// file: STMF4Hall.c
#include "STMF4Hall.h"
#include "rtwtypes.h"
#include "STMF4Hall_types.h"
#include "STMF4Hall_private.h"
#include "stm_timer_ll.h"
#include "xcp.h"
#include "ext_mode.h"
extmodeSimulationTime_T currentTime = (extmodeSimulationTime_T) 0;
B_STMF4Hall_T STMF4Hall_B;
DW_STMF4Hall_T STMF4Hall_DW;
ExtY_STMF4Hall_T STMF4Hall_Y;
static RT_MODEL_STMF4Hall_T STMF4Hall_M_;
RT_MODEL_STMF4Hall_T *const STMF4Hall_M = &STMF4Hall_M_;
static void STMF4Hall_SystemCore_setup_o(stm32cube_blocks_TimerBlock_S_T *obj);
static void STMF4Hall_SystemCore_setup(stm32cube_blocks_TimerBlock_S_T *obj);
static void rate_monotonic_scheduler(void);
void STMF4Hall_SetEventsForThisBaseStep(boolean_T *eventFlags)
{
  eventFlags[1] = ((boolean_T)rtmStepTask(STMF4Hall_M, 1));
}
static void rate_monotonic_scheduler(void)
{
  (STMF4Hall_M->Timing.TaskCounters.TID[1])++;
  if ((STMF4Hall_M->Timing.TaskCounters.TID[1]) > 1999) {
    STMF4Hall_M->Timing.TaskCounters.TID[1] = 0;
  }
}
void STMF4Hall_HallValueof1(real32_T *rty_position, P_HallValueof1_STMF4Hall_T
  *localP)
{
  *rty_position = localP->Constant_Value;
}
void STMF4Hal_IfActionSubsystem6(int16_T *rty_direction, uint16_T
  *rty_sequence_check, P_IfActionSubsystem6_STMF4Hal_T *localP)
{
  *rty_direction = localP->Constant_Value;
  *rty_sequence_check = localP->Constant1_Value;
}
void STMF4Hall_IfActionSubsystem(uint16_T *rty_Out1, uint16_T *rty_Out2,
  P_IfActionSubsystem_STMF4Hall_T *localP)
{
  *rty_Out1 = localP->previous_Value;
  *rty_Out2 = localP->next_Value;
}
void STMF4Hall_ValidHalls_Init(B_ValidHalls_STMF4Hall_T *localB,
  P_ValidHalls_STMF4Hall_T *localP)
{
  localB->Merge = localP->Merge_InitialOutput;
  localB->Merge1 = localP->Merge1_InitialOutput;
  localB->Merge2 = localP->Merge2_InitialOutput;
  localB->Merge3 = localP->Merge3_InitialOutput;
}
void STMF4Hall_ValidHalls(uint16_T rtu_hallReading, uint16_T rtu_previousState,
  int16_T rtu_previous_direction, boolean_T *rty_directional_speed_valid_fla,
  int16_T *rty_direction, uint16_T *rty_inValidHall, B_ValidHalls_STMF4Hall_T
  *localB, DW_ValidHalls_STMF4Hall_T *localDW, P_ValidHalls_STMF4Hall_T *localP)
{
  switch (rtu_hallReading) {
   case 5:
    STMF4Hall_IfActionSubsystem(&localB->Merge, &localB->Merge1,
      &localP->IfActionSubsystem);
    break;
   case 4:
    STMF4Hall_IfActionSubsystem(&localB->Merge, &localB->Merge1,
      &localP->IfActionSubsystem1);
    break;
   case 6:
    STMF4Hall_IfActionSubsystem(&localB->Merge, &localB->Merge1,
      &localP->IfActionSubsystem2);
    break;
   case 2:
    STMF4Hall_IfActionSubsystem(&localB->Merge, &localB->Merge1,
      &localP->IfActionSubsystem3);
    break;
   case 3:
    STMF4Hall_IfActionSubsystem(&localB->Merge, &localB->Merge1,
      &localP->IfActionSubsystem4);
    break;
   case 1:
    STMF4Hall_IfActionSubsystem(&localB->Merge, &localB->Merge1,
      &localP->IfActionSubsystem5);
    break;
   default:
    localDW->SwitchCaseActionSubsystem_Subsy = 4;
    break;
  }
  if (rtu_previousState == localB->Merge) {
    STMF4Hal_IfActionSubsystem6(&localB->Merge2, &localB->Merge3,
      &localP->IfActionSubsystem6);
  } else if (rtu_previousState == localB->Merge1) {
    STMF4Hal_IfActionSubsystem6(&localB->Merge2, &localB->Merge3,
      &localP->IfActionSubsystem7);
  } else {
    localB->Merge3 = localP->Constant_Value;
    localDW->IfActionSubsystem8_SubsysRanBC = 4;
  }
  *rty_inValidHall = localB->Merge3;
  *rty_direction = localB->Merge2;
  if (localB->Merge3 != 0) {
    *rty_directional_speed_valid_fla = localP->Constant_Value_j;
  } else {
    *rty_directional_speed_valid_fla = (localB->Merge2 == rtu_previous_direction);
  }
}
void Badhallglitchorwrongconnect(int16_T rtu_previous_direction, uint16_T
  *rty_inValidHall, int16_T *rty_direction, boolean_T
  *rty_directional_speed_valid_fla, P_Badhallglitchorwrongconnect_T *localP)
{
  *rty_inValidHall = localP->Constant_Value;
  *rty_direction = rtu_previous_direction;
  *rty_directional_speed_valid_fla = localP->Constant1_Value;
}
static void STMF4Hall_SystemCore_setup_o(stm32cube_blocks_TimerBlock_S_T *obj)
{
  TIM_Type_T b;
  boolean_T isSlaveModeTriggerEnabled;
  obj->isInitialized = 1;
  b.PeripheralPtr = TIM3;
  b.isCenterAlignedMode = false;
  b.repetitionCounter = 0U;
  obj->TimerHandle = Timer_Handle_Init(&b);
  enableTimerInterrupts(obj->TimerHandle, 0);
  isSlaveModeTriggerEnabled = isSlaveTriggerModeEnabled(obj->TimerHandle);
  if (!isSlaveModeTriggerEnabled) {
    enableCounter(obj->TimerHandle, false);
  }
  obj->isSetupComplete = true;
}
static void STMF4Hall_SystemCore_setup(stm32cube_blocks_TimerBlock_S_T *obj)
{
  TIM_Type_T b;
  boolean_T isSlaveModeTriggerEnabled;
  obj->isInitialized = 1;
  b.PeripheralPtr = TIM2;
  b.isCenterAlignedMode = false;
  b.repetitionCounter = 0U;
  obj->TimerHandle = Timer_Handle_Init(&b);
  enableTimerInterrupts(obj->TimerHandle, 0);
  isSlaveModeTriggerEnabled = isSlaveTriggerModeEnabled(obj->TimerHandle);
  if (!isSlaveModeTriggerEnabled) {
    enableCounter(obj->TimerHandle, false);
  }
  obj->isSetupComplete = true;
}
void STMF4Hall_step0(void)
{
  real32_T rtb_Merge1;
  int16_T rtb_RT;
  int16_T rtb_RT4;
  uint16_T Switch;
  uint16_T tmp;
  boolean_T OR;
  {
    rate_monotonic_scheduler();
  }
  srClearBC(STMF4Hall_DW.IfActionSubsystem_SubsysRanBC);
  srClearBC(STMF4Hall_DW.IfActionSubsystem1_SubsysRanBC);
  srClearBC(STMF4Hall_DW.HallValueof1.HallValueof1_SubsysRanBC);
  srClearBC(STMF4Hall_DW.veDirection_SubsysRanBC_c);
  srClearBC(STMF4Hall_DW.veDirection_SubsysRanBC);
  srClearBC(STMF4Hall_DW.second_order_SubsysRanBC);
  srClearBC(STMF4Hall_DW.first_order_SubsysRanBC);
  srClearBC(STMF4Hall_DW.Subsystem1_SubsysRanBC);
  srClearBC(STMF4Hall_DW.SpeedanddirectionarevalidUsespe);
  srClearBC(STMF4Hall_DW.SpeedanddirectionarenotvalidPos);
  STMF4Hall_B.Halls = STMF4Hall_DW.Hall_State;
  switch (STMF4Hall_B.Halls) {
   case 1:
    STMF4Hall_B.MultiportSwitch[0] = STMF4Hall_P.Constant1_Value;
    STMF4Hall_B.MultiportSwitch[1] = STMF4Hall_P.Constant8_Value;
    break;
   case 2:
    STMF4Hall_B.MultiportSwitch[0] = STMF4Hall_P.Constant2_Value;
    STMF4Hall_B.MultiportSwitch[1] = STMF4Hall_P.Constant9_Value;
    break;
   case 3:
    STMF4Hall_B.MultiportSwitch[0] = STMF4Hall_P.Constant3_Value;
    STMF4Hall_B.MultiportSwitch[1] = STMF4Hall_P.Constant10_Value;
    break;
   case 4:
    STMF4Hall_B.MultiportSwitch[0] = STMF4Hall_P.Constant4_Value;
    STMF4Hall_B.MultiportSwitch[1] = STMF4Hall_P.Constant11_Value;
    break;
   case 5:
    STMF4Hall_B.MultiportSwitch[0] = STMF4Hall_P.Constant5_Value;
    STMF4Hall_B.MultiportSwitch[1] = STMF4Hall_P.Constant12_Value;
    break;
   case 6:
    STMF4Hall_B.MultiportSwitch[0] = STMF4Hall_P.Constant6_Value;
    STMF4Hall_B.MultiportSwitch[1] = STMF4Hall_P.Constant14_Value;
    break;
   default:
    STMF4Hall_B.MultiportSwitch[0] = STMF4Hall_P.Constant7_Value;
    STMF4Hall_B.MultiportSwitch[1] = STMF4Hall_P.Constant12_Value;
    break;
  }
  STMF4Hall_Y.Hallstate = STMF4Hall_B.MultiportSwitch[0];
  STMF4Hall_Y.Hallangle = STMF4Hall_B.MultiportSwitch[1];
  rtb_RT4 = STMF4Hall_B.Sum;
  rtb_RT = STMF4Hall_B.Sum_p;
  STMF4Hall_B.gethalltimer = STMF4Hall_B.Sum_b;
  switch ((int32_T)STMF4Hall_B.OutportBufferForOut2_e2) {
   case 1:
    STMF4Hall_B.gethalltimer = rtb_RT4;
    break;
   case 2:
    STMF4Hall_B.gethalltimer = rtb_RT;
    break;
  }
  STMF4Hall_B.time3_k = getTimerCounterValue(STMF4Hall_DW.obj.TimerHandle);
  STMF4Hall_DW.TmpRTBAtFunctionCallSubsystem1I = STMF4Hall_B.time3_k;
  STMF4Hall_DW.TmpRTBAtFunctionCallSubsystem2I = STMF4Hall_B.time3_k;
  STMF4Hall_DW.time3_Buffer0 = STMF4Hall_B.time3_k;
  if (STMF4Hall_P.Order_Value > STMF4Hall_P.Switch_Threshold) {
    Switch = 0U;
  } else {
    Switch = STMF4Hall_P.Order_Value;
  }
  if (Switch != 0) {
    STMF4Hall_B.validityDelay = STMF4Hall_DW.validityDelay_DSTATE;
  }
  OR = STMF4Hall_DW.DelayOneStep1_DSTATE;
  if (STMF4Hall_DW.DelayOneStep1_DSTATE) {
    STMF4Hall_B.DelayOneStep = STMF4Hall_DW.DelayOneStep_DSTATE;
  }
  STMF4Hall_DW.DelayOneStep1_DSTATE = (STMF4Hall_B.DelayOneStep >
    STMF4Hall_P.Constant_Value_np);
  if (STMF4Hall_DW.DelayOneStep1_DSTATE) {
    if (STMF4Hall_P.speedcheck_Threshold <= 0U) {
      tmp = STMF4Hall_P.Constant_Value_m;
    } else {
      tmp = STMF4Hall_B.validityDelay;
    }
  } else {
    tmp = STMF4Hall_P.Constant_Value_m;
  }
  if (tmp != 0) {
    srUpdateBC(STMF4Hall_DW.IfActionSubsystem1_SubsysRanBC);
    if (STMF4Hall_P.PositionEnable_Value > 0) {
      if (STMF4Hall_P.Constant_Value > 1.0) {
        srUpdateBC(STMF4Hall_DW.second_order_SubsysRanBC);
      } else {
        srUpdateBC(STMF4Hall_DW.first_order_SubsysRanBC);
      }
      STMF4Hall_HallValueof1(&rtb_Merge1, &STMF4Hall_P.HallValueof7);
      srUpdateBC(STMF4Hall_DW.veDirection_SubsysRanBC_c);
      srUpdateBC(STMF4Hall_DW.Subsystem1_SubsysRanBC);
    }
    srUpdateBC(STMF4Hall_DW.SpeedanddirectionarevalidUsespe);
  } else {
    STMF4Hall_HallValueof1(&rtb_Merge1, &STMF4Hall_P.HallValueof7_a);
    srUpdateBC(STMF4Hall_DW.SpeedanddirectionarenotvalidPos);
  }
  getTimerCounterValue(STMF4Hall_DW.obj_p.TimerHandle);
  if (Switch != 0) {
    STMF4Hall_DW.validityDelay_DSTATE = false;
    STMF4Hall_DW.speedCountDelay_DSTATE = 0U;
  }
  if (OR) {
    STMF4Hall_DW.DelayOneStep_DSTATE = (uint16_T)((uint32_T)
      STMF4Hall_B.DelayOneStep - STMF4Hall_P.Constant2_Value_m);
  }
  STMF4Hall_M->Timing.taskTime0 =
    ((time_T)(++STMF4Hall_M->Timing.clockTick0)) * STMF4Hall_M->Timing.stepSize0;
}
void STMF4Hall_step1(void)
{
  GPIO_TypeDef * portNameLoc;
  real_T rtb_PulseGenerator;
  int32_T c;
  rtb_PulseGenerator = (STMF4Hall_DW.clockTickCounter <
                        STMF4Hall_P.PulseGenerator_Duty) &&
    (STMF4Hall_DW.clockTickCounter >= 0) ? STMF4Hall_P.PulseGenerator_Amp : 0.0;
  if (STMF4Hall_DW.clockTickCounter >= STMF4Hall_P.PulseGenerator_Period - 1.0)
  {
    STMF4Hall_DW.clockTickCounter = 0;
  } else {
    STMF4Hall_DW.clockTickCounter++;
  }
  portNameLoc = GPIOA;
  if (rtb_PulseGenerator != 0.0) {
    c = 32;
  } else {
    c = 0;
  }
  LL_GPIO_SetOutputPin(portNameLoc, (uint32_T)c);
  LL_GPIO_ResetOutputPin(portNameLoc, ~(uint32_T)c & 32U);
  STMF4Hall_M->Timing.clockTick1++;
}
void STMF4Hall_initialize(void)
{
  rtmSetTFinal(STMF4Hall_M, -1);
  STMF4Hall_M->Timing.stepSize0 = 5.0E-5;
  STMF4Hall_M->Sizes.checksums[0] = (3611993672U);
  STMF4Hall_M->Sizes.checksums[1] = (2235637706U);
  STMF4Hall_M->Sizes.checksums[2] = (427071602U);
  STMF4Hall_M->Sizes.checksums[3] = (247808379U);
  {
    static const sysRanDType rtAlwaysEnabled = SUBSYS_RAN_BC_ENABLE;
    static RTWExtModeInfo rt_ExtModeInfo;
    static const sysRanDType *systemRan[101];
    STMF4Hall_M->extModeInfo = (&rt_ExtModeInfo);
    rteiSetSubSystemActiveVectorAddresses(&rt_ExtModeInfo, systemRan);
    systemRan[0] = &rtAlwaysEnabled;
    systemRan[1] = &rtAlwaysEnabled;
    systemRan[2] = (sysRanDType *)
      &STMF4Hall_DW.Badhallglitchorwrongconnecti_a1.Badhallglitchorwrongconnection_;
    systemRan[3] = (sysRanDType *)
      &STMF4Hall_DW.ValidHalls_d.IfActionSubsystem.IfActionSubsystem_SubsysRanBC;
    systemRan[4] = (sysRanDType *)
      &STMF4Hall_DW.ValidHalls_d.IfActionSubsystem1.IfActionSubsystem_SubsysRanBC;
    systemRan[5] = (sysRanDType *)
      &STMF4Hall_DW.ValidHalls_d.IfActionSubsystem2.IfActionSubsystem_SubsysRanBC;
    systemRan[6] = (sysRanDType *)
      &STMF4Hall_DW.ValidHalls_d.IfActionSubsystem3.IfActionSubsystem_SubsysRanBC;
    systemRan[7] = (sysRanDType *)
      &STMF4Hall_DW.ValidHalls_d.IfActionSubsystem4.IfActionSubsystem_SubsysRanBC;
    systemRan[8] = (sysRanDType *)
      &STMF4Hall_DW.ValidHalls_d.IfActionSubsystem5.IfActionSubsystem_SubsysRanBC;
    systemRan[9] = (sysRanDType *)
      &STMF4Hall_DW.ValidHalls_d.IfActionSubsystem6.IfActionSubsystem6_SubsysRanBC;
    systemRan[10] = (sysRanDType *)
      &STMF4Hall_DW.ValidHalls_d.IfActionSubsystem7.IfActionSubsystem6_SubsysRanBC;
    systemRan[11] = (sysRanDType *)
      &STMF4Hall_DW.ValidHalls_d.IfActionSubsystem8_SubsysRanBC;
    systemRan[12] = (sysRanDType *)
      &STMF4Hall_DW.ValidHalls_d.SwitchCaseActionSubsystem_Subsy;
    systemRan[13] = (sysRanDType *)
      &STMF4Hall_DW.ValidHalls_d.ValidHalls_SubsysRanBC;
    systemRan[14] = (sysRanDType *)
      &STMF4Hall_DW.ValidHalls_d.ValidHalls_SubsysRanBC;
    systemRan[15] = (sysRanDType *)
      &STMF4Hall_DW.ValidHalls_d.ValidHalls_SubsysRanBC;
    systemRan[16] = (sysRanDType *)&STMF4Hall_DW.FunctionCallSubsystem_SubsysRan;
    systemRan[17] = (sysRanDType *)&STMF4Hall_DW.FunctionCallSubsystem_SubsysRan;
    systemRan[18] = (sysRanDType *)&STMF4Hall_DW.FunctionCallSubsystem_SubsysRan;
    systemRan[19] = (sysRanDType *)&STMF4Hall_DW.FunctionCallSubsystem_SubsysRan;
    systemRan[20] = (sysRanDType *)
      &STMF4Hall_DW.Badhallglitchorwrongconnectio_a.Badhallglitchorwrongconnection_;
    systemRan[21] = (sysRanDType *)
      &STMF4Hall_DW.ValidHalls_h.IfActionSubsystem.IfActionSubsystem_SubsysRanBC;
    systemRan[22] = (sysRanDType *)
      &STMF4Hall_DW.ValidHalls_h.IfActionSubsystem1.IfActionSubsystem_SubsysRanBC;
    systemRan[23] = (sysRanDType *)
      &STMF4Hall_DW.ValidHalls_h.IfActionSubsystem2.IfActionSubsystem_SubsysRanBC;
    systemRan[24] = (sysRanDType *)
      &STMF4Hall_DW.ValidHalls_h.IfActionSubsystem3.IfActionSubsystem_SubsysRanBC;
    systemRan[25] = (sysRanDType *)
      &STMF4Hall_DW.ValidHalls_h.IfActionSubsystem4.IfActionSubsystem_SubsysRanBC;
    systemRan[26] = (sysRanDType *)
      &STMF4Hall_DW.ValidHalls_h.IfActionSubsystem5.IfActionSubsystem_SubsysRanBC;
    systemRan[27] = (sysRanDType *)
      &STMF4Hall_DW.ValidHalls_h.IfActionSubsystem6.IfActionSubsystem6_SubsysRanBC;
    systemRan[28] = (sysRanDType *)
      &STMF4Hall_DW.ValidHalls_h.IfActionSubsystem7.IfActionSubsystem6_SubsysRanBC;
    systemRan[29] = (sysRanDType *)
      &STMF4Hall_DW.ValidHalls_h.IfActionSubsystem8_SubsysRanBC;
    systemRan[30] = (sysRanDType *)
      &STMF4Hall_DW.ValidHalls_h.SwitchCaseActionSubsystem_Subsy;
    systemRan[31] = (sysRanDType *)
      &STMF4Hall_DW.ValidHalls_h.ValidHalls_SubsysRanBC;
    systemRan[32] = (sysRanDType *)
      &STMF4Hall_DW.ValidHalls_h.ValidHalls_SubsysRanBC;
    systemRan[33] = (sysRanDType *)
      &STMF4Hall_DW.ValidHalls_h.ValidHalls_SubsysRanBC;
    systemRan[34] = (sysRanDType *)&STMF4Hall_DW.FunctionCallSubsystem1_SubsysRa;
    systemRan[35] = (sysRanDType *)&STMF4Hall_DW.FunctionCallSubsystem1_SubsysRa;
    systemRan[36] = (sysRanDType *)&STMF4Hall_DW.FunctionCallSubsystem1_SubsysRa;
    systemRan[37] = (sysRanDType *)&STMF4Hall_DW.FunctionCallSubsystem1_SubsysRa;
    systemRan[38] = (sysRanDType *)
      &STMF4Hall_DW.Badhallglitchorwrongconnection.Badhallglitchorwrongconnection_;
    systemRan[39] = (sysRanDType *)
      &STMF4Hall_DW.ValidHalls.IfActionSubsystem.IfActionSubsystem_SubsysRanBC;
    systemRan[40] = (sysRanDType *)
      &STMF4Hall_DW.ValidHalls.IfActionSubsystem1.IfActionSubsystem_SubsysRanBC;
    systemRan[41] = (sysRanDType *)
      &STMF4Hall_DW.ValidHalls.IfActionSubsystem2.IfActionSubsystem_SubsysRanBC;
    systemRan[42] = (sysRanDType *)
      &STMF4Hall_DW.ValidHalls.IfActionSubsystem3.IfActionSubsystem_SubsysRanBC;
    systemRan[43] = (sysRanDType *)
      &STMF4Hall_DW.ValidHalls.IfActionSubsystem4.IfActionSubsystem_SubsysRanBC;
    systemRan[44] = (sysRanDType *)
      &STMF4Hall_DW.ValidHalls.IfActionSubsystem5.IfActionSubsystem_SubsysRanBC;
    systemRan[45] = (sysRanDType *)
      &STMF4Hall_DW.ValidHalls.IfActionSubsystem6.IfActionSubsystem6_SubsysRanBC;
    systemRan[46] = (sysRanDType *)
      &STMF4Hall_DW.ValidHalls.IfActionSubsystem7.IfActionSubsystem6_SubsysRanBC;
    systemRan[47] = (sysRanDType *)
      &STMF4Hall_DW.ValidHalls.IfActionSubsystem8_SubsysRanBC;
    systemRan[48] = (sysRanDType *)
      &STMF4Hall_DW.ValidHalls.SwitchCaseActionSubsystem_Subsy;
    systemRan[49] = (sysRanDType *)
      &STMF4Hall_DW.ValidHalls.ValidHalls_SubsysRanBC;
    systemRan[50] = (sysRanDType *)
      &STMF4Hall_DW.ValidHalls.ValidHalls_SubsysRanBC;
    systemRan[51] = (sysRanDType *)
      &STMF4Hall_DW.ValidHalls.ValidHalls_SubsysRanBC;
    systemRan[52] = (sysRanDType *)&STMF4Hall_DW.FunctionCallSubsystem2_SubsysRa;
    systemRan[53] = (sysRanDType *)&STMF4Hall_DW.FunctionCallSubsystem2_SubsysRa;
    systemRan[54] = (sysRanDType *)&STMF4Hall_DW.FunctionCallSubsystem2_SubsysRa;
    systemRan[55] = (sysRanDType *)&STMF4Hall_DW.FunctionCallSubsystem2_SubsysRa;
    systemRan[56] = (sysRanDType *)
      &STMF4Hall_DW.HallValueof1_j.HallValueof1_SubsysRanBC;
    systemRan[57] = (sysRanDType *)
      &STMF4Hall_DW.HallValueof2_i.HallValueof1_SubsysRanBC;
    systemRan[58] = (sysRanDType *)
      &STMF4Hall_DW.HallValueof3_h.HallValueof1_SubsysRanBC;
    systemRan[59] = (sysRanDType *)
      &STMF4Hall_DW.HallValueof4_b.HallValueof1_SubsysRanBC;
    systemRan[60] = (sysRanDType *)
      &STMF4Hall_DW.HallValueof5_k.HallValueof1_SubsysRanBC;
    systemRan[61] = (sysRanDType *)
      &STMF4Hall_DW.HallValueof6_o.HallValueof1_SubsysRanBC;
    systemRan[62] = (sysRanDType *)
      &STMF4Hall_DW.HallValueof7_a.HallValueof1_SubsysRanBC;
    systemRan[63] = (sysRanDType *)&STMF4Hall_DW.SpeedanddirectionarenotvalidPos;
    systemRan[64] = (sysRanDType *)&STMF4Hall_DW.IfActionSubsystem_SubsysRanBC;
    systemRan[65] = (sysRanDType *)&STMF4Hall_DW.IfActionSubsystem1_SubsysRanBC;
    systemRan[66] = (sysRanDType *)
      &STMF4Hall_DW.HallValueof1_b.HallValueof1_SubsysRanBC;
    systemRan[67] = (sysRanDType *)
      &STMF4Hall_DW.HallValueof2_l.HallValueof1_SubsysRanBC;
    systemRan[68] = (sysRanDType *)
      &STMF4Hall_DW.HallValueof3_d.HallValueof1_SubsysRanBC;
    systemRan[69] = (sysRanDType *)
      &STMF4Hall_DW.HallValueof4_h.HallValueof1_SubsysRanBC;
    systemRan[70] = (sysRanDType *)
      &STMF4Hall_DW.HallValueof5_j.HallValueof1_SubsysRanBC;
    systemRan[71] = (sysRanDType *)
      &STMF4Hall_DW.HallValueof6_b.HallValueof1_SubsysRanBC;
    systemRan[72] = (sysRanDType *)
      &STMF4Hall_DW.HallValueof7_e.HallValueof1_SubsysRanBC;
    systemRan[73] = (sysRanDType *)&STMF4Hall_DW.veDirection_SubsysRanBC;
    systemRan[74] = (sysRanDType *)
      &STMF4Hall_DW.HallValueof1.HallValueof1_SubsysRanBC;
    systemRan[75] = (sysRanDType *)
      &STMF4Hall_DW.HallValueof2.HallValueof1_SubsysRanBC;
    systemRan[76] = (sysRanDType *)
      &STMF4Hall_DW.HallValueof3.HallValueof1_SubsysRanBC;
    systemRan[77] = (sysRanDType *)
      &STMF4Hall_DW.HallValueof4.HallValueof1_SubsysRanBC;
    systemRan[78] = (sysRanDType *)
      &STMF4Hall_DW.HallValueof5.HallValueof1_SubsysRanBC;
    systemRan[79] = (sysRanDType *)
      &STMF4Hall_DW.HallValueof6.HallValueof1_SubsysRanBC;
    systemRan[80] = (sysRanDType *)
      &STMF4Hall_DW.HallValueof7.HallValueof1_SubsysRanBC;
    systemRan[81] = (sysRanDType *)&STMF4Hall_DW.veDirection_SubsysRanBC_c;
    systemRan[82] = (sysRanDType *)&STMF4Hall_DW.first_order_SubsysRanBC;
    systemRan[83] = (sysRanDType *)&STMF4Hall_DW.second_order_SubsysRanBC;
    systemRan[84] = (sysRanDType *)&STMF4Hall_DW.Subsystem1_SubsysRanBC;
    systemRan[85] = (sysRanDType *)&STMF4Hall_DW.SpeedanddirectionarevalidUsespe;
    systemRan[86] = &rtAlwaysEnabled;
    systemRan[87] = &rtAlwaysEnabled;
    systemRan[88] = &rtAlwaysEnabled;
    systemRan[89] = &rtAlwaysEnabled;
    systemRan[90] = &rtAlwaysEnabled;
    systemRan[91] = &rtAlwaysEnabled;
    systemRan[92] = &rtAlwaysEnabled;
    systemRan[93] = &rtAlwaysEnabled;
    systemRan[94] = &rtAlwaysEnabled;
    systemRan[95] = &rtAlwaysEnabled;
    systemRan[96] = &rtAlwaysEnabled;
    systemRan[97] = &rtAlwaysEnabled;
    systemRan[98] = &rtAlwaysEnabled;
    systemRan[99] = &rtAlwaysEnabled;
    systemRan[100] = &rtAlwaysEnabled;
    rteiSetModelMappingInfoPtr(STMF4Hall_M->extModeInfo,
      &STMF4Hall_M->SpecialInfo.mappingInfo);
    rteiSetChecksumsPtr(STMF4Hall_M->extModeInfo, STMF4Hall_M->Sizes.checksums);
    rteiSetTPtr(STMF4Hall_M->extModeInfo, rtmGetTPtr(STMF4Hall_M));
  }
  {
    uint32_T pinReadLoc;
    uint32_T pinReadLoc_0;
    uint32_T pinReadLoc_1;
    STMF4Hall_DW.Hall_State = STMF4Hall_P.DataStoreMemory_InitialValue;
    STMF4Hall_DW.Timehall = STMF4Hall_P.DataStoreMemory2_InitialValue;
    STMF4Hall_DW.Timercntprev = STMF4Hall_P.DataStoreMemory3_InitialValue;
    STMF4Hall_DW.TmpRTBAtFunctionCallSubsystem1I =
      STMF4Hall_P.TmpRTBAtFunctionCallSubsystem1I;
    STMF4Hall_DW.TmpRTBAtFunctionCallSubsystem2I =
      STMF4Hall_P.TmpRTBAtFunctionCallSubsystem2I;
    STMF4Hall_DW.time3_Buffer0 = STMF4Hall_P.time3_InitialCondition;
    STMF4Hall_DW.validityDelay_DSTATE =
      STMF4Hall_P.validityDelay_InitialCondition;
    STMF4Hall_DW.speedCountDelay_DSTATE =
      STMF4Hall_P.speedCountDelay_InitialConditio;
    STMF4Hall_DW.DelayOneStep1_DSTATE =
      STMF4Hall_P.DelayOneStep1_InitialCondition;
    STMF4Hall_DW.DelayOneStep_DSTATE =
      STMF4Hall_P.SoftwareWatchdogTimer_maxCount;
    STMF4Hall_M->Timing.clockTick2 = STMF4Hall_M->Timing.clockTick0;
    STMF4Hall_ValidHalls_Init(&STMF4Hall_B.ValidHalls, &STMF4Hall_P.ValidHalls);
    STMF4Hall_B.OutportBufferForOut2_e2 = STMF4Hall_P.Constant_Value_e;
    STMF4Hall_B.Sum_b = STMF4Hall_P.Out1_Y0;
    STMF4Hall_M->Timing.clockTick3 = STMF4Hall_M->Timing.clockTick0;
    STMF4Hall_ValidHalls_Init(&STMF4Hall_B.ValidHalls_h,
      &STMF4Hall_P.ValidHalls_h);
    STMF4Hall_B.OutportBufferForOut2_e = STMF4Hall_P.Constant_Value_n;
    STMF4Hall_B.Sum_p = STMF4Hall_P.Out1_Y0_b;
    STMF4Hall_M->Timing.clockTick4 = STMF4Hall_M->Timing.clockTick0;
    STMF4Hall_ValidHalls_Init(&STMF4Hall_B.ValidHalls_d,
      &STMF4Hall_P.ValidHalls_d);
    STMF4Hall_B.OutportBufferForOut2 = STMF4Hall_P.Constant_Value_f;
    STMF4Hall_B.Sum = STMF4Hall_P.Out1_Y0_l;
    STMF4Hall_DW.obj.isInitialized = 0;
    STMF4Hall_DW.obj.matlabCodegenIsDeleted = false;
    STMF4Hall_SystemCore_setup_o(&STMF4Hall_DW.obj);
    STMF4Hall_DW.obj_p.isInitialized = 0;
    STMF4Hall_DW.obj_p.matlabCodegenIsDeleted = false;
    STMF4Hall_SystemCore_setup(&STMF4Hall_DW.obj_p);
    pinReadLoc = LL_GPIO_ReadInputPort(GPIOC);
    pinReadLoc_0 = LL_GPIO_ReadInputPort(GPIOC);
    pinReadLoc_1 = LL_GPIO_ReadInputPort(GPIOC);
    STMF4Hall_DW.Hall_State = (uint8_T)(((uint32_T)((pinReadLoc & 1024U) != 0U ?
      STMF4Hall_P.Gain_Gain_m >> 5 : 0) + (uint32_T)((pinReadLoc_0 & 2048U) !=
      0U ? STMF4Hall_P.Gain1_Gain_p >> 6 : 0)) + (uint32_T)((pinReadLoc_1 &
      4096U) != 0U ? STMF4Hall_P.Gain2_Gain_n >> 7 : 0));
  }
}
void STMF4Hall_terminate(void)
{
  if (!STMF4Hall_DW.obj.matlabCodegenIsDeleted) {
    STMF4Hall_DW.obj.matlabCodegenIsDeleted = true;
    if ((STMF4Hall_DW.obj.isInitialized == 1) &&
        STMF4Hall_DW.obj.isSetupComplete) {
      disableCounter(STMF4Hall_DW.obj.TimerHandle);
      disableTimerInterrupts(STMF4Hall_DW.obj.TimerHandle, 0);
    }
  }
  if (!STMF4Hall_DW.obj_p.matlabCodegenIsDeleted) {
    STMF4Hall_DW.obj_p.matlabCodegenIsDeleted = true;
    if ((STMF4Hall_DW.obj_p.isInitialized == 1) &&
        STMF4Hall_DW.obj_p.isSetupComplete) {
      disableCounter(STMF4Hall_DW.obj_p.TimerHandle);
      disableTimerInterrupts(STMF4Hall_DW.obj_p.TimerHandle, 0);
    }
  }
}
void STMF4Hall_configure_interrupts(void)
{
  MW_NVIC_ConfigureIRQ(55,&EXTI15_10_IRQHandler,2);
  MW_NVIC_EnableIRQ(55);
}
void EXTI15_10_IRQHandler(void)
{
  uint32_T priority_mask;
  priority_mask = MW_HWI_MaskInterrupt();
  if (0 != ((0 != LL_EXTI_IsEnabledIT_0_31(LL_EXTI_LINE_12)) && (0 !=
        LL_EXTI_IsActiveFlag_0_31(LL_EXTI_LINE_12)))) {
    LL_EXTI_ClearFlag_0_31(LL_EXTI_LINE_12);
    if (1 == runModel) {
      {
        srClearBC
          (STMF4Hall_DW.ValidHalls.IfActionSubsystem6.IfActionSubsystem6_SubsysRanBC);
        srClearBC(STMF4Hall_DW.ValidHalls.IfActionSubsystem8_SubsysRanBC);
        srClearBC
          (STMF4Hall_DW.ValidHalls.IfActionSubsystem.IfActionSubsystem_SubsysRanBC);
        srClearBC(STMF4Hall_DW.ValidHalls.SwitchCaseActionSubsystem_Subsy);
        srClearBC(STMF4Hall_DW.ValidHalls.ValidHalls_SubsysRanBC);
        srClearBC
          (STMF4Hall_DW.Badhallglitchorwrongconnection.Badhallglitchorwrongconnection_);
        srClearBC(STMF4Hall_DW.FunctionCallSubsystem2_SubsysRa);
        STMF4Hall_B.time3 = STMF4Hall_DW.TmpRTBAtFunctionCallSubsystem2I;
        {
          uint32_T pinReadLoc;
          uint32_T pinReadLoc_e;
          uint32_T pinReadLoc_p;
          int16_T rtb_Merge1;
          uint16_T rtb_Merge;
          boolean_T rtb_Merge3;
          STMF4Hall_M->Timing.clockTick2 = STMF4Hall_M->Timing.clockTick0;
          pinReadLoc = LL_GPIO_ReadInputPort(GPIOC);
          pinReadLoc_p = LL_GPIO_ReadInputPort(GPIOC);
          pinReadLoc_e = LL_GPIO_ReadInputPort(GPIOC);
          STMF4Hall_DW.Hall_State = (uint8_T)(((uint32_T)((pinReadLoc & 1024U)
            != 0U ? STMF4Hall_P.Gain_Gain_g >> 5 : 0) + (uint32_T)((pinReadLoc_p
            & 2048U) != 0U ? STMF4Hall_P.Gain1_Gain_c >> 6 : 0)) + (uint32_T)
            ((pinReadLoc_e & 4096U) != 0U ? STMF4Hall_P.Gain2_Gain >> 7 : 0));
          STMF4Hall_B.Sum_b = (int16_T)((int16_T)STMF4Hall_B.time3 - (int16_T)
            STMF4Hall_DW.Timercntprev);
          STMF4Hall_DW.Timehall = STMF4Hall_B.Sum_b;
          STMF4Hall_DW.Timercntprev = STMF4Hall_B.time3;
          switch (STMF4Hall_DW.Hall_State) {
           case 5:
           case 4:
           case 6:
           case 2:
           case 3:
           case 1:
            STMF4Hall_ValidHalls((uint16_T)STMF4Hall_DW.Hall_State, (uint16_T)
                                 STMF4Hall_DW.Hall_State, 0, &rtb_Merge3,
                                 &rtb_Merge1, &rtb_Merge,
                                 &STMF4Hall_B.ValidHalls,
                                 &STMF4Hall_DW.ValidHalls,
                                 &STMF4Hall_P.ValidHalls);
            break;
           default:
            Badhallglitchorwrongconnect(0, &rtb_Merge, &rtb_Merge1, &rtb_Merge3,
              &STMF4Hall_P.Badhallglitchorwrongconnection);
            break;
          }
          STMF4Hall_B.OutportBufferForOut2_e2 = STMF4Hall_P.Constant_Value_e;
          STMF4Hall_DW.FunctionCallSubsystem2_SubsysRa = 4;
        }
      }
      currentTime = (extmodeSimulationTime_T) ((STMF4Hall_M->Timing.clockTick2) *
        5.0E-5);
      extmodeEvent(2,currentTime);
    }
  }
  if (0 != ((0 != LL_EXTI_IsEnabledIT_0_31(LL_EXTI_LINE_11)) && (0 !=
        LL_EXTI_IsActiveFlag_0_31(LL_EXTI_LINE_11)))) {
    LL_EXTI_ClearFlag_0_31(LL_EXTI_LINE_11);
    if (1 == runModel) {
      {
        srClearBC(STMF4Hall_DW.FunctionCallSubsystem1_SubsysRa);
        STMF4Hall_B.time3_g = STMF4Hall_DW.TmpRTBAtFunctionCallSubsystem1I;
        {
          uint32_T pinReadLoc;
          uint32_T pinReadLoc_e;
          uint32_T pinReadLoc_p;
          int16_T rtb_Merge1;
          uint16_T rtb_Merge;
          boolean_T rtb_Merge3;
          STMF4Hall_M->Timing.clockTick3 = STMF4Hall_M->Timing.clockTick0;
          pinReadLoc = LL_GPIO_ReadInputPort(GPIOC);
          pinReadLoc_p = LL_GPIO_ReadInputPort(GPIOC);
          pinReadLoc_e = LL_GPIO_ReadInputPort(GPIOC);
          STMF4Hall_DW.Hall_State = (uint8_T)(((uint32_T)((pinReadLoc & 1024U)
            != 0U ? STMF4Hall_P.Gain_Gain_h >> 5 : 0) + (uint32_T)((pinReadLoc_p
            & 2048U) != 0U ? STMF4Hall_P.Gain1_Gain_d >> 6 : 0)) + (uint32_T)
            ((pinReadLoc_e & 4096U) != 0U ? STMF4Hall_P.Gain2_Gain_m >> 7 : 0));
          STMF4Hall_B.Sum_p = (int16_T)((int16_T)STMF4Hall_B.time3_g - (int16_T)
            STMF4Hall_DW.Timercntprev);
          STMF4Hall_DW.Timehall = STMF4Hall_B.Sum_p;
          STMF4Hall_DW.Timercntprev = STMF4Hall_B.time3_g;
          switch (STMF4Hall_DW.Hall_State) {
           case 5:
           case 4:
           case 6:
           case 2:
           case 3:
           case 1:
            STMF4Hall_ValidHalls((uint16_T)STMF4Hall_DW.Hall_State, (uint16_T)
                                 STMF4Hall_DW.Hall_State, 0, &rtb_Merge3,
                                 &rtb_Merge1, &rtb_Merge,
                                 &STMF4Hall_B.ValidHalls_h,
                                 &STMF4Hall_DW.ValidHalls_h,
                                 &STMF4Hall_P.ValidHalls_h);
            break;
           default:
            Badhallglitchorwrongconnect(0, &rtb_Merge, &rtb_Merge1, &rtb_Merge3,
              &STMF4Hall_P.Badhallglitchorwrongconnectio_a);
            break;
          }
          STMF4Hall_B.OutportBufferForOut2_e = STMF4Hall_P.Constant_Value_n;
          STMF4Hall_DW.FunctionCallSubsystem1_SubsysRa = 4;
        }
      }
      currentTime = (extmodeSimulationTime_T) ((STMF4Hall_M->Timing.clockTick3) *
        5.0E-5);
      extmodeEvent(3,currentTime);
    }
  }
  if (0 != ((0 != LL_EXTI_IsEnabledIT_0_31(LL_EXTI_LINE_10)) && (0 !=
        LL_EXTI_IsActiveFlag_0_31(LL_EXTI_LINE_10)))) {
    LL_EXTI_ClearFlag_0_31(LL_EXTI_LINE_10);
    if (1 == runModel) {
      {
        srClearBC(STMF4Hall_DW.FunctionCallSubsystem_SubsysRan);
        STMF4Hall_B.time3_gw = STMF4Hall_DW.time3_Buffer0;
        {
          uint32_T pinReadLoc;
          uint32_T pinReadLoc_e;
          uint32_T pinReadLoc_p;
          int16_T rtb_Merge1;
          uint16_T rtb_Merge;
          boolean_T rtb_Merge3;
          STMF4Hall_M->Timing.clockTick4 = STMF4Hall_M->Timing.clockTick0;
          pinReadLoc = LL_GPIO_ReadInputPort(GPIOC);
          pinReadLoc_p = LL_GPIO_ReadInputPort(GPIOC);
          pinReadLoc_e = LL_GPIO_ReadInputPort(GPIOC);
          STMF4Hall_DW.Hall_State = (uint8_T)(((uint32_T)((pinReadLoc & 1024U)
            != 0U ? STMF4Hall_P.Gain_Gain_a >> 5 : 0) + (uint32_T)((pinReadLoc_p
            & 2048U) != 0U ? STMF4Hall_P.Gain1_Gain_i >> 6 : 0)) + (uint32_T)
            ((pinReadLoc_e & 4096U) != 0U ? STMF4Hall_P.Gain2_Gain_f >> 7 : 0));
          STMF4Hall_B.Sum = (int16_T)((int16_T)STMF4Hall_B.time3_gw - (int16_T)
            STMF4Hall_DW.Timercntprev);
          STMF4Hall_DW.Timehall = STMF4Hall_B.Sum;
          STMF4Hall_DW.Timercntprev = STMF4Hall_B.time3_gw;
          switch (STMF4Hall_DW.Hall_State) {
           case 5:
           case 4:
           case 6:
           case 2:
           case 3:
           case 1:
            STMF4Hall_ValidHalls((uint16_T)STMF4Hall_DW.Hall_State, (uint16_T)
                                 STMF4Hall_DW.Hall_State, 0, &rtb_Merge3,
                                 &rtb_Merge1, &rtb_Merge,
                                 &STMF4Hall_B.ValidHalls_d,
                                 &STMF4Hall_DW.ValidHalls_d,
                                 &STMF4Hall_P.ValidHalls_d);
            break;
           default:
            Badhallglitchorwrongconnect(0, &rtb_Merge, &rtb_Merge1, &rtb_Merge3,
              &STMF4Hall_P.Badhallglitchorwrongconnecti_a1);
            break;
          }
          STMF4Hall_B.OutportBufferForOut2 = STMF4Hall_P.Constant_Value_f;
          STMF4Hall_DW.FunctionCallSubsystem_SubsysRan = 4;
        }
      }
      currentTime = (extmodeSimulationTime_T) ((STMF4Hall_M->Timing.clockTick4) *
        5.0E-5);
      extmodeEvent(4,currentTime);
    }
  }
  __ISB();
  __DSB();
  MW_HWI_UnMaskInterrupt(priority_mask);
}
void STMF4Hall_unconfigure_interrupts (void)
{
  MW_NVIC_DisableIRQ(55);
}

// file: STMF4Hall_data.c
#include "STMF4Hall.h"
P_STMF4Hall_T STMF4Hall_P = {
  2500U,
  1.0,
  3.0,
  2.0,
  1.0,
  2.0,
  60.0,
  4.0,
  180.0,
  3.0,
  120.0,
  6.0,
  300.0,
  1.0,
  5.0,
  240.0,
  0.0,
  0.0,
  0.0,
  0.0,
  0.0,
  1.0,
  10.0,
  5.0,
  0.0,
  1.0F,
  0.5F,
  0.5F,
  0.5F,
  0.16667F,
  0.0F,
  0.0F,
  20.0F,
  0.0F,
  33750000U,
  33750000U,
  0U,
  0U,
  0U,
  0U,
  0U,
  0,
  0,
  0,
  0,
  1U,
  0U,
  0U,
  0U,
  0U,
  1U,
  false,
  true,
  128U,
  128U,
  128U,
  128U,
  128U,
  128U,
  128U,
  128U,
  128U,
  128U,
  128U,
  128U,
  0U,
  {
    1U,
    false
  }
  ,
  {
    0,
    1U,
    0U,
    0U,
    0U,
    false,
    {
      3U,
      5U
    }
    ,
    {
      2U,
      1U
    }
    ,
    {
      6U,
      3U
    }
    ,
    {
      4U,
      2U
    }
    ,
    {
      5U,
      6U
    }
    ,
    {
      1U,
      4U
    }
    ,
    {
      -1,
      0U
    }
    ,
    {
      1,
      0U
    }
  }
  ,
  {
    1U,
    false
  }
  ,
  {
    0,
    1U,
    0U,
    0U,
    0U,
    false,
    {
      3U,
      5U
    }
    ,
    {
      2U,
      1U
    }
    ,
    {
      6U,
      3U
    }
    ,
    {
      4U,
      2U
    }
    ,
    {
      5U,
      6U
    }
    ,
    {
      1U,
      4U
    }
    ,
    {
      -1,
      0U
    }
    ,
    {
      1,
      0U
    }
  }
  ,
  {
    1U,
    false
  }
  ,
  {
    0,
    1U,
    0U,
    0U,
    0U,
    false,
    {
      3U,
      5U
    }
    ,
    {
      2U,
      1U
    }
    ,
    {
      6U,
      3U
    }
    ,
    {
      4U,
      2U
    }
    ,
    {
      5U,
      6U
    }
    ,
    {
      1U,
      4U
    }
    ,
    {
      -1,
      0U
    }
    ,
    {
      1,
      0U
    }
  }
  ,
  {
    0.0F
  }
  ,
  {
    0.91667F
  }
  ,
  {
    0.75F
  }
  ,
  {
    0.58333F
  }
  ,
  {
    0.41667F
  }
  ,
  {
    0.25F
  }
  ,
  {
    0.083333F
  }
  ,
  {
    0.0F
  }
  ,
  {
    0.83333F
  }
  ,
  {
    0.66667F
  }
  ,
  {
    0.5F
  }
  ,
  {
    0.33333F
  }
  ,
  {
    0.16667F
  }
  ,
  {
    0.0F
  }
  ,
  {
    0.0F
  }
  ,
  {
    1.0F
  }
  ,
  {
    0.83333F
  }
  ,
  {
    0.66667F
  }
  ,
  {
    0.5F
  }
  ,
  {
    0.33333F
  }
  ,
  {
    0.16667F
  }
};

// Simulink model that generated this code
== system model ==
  Hallstate : Outport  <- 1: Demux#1
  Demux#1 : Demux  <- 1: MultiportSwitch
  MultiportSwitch : MultiPortSwitch  Inputs=6  <- 1: DataStoreRead#1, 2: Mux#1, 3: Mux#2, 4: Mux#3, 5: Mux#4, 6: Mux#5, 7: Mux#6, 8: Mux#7
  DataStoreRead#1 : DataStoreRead  DataStoreName=Hall_State  Indices=1
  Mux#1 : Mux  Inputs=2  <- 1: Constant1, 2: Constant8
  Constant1 : Constant  Value=2
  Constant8 : Constant  Value=60
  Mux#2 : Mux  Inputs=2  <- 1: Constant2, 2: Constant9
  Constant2 : Constant  Value=4
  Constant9 : Constant  Value=180
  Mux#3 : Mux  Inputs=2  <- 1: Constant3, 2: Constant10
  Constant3 : Constant  Value=3
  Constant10 : Constant  Value=120
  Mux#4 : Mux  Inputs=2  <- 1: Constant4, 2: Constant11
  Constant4 : Constant  Value=6
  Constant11 : Constant  Value=300
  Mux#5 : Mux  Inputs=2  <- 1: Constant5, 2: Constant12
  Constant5 : Constant
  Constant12 : Constant  Value=0
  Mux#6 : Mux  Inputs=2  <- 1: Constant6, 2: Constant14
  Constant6 : Constant  Value=5
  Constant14 : Constant  Value=240
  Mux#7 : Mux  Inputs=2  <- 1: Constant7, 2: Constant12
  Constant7 : Constant  Value=0
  Hallangle : Outport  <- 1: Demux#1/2
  Timer : stm32blockslib/Timer
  MultiPortSwitch#1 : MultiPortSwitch  <- 1: DataStoreRead#2, 2: RT4, 3: RT, 4: RateTransition#1
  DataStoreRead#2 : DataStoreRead  DataStoreName=Exitnumber  Indices=1
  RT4 : RateTransition  <- 1: FunctionCallSubsystem
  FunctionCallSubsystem : Subsystem  <- 1: Timer#1, Trigger: HardwareInterrupt#1/3
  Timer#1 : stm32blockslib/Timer
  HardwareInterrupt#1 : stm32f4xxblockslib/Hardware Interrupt
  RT : RateTransition  <- 1: FunctionCallSubsystem1
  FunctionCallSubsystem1 : Subsystem  <- 1: Timer#1, Trigger: HardwareInterrupt#1/2
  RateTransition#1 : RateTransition  <- 1: FunctionCallSubsystem2
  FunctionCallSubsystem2 : Subsystem  <- 1: Timer#1, Trigger: HardwareInterrupt#1
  DigitalPortWrite#1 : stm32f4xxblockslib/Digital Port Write  <- 1: PulseGenerator
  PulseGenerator : DiscretePulseGenerator  Period=10  PulseWidth=5
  DataStoreMemory : DataStoreMemory  DataStoreName=Hall_State
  DataStoreMemory2 : DataStoreMemory  DataStoreName=Timehall
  DataStoreMemory3 : DataStoreMemory  DataStoreName=Timercntprev
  Subsystem#1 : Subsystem
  DataStoreWrite#1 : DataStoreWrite  DataStoreName=Exitnumber  Indices=1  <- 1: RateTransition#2
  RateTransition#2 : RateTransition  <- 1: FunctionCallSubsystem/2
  DataStoreWrite#2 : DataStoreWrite  DataStoreName=Exitnumber  Indices=1  <- 1: RateTransition#3
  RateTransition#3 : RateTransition  <- 1: FunctionCallSubsystem2/2
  DataStoreWrite#3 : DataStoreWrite  DataStoreName=Exitnumber  Indices=1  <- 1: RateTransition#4
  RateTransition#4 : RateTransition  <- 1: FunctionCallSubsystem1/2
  DataStoreMemory#1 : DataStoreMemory  DataStoreName=Timercnt
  DataStoreMemory#2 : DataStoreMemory  DataStoreName=Diection_hall
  DataStoreMemory#3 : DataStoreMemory  DataStoreName=Exitnumber
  HallSpeedandPosition#1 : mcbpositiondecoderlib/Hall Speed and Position
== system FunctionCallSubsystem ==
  Inport#1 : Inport
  TriggerPort#1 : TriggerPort  TriggerType=function-call
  Out1 : Outport  <- 1: Sum
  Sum : Sum  Inputs=+-  <- 1: DataTypeConversion#1, 2: DataTypeConversion#2
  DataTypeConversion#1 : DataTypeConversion  <- 1: Inport#1
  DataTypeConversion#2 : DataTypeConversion  <- 1: DataStoreRead#3
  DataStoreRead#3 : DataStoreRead  DataStoreName=Timercntprev  Indices=1
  Out2 : Outport  <- 1: Constant
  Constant : Constant
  HallValidity#1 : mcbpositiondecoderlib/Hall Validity  <- 1: Sum#1, 2: DataStoreRead#4, 3: Sum
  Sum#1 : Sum  Inputs=+++  <- 1: Gain, 2: Gain1, 3: Gain2
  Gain : Gain  Gain=4  <- 1: DigitalPortRead#1
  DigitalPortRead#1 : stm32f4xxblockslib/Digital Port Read
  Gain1 : Gain  Gain=2  <- 1: DigitalPortRead#2
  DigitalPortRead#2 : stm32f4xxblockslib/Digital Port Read
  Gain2 : Gain  <- 1: DigitalPortRead#3
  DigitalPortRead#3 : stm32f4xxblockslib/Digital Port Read
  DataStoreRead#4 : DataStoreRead  DataStoreName=Hall_State  Indices=1
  DataStoreWrite#4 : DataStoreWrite  DataStoreName=Hall_State  Indices=1  <- 1: Sum#1
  DataStoreWrite#5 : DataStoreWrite  DataStoreName=Timehall  Indices=1  <- 1: Sum
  DataStoreWrite#6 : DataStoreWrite  DataStoreName=Timercntprev  Indices=1  <- 1: Inport#1
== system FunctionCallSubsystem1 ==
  Inport#2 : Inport
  TriggerPort#2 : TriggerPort  TriggerType=function-call
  Outport#1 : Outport  <- 1: Sum#2
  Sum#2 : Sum  Inputs=+-  <- 1: DataTypeConversion#3, 2: DataTypeConversion#4
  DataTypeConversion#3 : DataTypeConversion  <- 1: Inport#2
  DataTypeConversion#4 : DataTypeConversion  <- 1: DataStoreRead#5
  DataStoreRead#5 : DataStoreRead  DataStoreName=Timercntprev  Indices=1
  Outport#2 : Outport  <- 1: Constant#1
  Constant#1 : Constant  Value=2
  HallValidity#2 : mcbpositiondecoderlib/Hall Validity  <- 1: Sum#3, 2: DataStoreRead#6, 3: Sum#2
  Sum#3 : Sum  Inputs=+++  <- 1: Gain#1, 2: Gain#2, 3: Gain#3
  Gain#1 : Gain  Gain=4  <- 1: DigitalPortRead#4
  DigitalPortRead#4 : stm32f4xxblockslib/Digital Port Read
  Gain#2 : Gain  Gain=2  <- 1: DigitalPortRead#5
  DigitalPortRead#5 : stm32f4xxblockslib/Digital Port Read
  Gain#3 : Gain  <- 1: DigitalPortRead#6
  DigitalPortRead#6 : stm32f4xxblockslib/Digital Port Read
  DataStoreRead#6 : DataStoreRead  DataStoreName=Hall_State  Indices=1
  DataStoreWrite#7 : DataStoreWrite  DataStoreName=Hall_State  Indices=1  <- 1: Sum#3
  DataStoreWrite#8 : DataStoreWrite  DataStoreName=Timehall  Indices=1  <- 1: Sum#2
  DataStoreWrite#9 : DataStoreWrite  DataStoreName=Timercntprev  Indices=1  <- 1: Inport#2
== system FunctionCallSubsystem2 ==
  Inport#3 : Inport
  TriggerPort#3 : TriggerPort  TriggerType=function-call
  Outport#3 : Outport  <- 1: Sum#4
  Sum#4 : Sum  Inputs=+-  <- 1: DataTypeConversion#5, 2: DataTypeConversion#6
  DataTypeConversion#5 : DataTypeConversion  <- 1: Inport#3
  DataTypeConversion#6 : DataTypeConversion  <- 1: DataStoreRead#7
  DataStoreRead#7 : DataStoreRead  DataStoreName=Timercntprev  Indices=1
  Outport#4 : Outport  <- 1: Constant#2
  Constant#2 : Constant  Value=3
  HallValidity#3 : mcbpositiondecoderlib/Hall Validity  <- 1: Sum#5, 2: DataStoreRead#8, 3: Sum#4
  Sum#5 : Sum  Inputs=+++  <- 1: Gain#4, 2: Gain#5, 3: Gain#6
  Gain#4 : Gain  Gain=4  <- 1: DigitalPortRead#7
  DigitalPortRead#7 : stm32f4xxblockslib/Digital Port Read
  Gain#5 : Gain  Gain=2  <- 1: DigitalPortRead#8
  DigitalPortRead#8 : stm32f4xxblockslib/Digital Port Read
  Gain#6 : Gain  <- 1: DigitalPortRead#9
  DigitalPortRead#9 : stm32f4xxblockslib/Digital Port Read
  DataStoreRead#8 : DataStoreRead  DataStoreName=Hall_State  Indices=1
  DataStoreWrite#10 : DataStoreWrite  DataStoreName=Hall_State  Indices=1  <- 1: Sum#5
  DataStoreWrite#11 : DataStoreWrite  DataStoreName=Timehall  Indices=1  <- 1: Sum#4
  DataStoreWrite#12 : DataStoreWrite  DataStoreName=Timercntprev  Indices=1  <- 1: Inport#3
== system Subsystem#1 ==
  DataStoreWrite#13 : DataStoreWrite  DataStoreName=Hall_State  Indices=1  <- 1: Sum#6
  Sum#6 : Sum  Inputs=+++  <- 1: Gain#7, 2: Gain#8, 3: Gain#9
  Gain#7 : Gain  Gain=4  <- 1: DigitalPortRead#10
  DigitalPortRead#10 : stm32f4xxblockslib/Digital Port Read
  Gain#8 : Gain  Gain=2  <- 1: DigitalPortRead#11
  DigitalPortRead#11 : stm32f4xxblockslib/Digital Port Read
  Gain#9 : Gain  <- 1: DigitalPortRead#12
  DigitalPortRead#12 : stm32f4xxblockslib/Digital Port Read
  EventListener#1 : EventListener
